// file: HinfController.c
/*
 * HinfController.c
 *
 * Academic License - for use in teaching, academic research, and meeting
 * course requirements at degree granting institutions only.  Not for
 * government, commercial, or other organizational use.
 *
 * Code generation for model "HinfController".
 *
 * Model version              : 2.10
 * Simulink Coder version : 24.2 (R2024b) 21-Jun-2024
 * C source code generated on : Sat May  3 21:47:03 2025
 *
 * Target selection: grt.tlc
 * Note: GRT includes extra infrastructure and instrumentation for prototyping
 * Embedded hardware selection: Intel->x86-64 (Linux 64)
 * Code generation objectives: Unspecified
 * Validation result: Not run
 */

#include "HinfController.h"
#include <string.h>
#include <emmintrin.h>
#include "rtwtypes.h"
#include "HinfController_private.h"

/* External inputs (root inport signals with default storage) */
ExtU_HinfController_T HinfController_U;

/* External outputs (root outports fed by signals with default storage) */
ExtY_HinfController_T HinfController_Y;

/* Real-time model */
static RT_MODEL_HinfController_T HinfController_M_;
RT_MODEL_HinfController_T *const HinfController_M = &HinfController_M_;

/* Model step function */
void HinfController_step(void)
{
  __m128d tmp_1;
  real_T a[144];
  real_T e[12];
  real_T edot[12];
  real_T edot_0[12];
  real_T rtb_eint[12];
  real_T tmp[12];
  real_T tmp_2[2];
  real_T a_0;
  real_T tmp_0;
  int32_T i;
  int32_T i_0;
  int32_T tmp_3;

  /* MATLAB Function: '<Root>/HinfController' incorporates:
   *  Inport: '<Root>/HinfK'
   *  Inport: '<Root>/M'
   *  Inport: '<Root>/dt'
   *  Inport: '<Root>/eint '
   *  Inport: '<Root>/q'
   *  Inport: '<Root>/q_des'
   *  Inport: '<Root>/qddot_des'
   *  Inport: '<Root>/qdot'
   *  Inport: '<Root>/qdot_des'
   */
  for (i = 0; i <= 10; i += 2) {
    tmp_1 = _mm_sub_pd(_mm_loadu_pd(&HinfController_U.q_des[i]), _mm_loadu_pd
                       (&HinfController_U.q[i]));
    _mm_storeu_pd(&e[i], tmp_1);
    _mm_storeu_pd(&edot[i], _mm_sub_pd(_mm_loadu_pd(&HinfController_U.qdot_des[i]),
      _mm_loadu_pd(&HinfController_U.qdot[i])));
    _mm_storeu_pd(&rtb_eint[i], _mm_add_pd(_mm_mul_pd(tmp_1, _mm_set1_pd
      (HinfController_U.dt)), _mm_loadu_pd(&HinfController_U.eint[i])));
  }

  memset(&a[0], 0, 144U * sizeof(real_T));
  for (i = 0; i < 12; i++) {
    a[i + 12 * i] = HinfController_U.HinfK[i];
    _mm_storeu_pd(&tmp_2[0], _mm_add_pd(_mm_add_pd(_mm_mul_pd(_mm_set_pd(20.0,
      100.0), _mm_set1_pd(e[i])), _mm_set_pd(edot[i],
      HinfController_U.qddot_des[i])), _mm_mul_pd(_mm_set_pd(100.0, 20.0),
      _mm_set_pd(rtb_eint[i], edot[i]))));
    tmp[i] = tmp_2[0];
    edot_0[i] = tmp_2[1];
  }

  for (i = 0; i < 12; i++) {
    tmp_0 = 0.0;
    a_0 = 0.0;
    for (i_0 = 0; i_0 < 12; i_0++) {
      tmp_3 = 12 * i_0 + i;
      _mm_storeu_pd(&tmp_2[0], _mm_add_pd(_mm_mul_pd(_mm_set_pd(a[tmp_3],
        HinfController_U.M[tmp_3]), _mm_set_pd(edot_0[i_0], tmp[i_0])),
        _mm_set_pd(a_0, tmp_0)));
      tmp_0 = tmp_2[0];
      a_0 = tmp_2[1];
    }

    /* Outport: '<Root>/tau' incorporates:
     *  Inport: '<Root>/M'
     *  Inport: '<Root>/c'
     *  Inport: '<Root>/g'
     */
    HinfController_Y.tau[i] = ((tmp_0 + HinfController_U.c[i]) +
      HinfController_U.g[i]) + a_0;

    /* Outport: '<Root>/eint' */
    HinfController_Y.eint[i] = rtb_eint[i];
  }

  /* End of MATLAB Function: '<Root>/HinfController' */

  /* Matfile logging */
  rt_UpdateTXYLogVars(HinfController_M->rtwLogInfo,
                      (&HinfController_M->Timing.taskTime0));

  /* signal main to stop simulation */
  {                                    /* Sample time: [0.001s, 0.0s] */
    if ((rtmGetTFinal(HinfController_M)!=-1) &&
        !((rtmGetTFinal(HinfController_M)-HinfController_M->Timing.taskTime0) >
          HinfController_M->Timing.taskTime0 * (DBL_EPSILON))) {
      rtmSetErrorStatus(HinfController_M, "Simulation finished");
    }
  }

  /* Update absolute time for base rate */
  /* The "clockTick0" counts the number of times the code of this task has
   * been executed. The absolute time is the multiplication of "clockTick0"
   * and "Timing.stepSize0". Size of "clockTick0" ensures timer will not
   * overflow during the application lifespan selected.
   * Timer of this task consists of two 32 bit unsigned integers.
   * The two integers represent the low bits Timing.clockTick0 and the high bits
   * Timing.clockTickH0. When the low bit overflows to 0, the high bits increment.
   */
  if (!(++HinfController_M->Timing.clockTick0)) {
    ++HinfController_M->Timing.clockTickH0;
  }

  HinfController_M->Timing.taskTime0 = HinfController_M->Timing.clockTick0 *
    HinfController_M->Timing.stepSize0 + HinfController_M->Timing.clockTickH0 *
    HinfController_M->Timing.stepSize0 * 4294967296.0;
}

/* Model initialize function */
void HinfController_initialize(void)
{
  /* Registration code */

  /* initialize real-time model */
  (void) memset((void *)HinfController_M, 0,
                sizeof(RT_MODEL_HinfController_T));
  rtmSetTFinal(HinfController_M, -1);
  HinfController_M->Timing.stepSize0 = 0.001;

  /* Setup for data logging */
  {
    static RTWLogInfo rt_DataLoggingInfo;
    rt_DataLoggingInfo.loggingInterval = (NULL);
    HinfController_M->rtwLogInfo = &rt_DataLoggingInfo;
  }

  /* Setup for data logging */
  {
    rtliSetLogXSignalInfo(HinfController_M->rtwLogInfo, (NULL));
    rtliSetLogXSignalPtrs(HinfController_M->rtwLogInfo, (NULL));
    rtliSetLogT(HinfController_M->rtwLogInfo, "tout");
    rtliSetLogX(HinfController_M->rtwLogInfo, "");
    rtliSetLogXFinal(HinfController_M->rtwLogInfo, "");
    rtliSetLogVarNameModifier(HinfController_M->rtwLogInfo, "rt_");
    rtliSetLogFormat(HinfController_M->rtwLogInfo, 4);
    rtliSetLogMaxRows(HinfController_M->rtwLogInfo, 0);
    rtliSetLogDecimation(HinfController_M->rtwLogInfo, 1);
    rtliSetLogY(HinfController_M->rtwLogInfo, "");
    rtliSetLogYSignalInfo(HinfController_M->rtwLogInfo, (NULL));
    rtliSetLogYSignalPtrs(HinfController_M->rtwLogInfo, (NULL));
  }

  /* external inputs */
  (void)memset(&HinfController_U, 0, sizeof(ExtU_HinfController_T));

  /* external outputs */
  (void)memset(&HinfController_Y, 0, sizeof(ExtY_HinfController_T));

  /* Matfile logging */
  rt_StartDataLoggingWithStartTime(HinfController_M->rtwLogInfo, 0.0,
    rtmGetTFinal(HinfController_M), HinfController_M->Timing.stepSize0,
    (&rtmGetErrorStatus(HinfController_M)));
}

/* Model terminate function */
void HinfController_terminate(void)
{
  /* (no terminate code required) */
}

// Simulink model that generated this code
simulink model "HinfController"  (R2024b)
settings: Solver=FixedStepDiscrete  StartTime=0.0  StopTime=Inf  FixedStep=0.001  RelTol=1e-3
model workspace (MAT data in the model file):
  robot : robotics.RigidBodyTree (value not decoded)

== system HinfController ==
  M : Inport  PortDimensions=[12,12]
  g : Inport  Port=2  PortDimensions=12
  c : Inport  Port=3  PortDimensions=12
  q : Inport  Port=4  PortDimensions=12
  qdot : Inport  Port=5  PortDimensions=12
  q_des : Inport  Port=6  PortDimensions=12
  qdot_des : Inport  Port=7  PortDimensions=12
  qddot_des : Inport  Port=8  PortDimensions=12
  HinfK : Inport  Port=9  PortDimensions=12
  dt : Inport  Port=10
  "eint " : Inport  Port=11
  HinfController : MATLAB Function  TreatAsAtomicUnit=on
  tau : Outport
  eint : Outport  Port=2
  wires:
  M/1 -> HinfController/1(M)
  qdot_des/1 -> HinfController/7(qdot_des)
  g/1 -> HinfController/3(g)
  c/1 -> HinfController/2(c)
  q/1 -> HinfController/4(q)
  qdot/1 -> HinfController/5(qdot)
  q_des/1 -> HinfController/6(q_des)
  qddot_des/1 -> HinfController/8(qddot_des)
  HinfController/1(tau) -> tau/1
  HinfController/2(eint) -> eint/1
  HinfK/1 -> HinfController/11(HinfK)
  dt/1 -> HinfController/9(dt)
  "eint "/1 -> HinfController/10("eint ")

== matlab function HinfController/HinfController ==
function [tau,eint]  = HinfController(M,c,g,q,qdot,q_des,qdot_des,qddot_des,dt,eint,HinfK)

e = q_des-q;
edot = qdot_des-qdot;
eint = eint+e.*dt;
qddot_ref =qddot_des+100*e+20*edot;

tau = M*qddot_ref+c+g+diag(HinfK)*(edot+20*e+100*eint);
